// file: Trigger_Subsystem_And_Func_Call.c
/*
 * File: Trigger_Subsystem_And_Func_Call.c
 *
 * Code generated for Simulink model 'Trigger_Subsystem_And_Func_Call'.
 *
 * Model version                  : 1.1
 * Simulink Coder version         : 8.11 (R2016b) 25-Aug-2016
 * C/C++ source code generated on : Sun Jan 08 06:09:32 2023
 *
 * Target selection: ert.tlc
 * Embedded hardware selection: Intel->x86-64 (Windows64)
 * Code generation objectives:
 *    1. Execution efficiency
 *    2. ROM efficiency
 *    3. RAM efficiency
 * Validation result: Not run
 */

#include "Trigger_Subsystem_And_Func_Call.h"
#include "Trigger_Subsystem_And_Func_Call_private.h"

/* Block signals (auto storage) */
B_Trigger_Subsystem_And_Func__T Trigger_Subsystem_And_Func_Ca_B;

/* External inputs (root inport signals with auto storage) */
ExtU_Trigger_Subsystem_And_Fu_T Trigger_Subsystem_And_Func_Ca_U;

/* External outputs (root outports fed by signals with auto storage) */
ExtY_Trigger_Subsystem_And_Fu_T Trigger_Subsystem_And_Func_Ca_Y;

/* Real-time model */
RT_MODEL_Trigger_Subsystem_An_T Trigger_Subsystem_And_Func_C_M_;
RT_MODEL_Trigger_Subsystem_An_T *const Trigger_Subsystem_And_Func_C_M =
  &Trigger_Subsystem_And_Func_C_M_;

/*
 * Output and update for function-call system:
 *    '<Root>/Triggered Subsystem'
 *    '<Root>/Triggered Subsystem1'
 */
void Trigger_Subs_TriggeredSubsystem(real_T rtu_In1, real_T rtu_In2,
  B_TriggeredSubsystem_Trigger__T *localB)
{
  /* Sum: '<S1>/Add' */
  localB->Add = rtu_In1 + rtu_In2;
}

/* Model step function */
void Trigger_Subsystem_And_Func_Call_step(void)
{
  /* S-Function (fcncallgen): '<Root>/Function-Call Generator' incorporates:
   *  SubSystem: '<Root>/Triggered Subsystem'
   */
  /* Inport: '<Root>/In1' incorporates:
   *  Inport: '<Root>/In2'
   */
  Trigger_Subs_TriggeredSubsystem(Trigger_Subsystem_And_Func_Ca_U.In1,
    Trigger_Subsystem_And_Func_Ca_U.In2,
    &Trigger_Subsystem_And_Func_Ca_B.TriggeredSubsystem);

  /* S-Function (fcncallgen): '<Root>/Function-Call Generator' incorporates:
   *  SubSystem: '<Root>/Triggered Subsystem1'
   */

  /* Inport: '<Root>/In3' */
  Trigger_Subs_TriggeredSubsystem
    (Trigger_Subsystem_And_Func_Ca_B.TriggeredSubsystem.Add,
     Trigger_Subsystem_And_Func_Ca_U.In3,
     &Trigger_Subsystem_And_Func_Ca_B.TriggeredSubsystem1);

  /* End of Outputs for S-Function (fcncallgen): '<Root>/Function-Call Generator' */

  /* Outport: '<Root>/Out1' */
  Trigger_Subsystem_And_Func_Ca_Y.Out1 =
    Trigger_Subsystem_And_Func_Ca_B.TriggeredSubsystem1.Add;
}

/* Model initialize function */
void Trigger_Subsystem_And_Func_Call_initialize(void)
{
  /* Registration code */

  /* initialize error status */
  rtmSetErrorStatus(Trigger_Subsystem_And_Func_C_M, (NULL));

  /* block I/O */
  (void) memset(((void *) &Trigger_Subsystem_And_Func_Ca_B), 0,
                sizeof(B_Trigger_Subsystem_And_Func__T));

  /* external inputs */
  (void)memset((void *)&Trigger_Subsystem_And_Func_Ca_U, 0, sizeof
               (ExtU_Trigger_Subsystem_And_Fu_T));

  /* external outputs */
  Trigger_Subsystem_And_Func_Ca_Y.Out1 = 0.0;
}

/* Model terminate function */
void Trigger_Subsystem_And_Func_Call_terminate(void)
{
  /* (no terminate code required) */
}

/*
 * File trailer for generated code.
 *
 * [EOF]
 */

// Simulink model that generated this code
simulink model "Trigger_Subsystem_And_Func_Call"  (R2016b)
settings: Solver=FixedStepDiscrete  StartTime=0.0  StopTime=10.0  RelTol=1e-3
libraries: simulink x1

== system Trigger_Subsystem_And_Func_Call ==
  In1 : Inport
  In2 : Inport  Port=2
  In3 : Inport  Port=3
  Function-Call Generator : simulink/Ports & Subsystems/Function-Call Generator  sample_time=1  numberOfIterations=1
  Function-Call Split : FunctionCallSplit  NumOutputPorts=2
  Triggered Subsystem : Subsystem  TreatAsAtomicUnit=on
  Triggered Subsystem1 : Subsystem  TreatAsAtomicUnit=on
  Out1 : Outport
  wires:
  In1/1 -> Triggered Subsystem/1(In1)
  In2/1 -> Triggered Subsystem/2(In2)
  Triggered Subsystem/1(Out1) -> Triggered Subsystem1/1(In1)
  Function-Call Generator/1 -> Function-Call Split/1
  In3/1 -> Triggered Subsystem1/2(In2)
  Function-Call Split/1 -> Triggered Subsystem/Trigger
  Function-Call Split/2 -> Triggered Subsystem1/Trigger
  Triggered Subsystem1/1(Out1) -> Out1/1

== system Trigger_Subsystem_And_Func_Call/Triggered Subsystem ==
  In1 : Inport
  In2 : Inport  Port=2
  Trigger : TriggerPort  TriggerType=function-call  VariantControl=Variant
  Add : Sum
  Out1 : Outport
  wires:
  In1/1 -> Add/1
  In2/1 -> Add/2
  Add/1 -> Out1/1

== system Trigger_Subsystem_And_Func_Call/Triggered Subsystem1 ==
  In1 : Inport
  In2 : Inport  Port=2
  Trigger : TriggerPort  TriggerType=function-call  VariantControl=Variant
  Add : Sum
  Out1 : Outport
  wires:
  In1/1 -> Add/1
  In2/1 -> Add/2
  Add/1 -> Out1/1
